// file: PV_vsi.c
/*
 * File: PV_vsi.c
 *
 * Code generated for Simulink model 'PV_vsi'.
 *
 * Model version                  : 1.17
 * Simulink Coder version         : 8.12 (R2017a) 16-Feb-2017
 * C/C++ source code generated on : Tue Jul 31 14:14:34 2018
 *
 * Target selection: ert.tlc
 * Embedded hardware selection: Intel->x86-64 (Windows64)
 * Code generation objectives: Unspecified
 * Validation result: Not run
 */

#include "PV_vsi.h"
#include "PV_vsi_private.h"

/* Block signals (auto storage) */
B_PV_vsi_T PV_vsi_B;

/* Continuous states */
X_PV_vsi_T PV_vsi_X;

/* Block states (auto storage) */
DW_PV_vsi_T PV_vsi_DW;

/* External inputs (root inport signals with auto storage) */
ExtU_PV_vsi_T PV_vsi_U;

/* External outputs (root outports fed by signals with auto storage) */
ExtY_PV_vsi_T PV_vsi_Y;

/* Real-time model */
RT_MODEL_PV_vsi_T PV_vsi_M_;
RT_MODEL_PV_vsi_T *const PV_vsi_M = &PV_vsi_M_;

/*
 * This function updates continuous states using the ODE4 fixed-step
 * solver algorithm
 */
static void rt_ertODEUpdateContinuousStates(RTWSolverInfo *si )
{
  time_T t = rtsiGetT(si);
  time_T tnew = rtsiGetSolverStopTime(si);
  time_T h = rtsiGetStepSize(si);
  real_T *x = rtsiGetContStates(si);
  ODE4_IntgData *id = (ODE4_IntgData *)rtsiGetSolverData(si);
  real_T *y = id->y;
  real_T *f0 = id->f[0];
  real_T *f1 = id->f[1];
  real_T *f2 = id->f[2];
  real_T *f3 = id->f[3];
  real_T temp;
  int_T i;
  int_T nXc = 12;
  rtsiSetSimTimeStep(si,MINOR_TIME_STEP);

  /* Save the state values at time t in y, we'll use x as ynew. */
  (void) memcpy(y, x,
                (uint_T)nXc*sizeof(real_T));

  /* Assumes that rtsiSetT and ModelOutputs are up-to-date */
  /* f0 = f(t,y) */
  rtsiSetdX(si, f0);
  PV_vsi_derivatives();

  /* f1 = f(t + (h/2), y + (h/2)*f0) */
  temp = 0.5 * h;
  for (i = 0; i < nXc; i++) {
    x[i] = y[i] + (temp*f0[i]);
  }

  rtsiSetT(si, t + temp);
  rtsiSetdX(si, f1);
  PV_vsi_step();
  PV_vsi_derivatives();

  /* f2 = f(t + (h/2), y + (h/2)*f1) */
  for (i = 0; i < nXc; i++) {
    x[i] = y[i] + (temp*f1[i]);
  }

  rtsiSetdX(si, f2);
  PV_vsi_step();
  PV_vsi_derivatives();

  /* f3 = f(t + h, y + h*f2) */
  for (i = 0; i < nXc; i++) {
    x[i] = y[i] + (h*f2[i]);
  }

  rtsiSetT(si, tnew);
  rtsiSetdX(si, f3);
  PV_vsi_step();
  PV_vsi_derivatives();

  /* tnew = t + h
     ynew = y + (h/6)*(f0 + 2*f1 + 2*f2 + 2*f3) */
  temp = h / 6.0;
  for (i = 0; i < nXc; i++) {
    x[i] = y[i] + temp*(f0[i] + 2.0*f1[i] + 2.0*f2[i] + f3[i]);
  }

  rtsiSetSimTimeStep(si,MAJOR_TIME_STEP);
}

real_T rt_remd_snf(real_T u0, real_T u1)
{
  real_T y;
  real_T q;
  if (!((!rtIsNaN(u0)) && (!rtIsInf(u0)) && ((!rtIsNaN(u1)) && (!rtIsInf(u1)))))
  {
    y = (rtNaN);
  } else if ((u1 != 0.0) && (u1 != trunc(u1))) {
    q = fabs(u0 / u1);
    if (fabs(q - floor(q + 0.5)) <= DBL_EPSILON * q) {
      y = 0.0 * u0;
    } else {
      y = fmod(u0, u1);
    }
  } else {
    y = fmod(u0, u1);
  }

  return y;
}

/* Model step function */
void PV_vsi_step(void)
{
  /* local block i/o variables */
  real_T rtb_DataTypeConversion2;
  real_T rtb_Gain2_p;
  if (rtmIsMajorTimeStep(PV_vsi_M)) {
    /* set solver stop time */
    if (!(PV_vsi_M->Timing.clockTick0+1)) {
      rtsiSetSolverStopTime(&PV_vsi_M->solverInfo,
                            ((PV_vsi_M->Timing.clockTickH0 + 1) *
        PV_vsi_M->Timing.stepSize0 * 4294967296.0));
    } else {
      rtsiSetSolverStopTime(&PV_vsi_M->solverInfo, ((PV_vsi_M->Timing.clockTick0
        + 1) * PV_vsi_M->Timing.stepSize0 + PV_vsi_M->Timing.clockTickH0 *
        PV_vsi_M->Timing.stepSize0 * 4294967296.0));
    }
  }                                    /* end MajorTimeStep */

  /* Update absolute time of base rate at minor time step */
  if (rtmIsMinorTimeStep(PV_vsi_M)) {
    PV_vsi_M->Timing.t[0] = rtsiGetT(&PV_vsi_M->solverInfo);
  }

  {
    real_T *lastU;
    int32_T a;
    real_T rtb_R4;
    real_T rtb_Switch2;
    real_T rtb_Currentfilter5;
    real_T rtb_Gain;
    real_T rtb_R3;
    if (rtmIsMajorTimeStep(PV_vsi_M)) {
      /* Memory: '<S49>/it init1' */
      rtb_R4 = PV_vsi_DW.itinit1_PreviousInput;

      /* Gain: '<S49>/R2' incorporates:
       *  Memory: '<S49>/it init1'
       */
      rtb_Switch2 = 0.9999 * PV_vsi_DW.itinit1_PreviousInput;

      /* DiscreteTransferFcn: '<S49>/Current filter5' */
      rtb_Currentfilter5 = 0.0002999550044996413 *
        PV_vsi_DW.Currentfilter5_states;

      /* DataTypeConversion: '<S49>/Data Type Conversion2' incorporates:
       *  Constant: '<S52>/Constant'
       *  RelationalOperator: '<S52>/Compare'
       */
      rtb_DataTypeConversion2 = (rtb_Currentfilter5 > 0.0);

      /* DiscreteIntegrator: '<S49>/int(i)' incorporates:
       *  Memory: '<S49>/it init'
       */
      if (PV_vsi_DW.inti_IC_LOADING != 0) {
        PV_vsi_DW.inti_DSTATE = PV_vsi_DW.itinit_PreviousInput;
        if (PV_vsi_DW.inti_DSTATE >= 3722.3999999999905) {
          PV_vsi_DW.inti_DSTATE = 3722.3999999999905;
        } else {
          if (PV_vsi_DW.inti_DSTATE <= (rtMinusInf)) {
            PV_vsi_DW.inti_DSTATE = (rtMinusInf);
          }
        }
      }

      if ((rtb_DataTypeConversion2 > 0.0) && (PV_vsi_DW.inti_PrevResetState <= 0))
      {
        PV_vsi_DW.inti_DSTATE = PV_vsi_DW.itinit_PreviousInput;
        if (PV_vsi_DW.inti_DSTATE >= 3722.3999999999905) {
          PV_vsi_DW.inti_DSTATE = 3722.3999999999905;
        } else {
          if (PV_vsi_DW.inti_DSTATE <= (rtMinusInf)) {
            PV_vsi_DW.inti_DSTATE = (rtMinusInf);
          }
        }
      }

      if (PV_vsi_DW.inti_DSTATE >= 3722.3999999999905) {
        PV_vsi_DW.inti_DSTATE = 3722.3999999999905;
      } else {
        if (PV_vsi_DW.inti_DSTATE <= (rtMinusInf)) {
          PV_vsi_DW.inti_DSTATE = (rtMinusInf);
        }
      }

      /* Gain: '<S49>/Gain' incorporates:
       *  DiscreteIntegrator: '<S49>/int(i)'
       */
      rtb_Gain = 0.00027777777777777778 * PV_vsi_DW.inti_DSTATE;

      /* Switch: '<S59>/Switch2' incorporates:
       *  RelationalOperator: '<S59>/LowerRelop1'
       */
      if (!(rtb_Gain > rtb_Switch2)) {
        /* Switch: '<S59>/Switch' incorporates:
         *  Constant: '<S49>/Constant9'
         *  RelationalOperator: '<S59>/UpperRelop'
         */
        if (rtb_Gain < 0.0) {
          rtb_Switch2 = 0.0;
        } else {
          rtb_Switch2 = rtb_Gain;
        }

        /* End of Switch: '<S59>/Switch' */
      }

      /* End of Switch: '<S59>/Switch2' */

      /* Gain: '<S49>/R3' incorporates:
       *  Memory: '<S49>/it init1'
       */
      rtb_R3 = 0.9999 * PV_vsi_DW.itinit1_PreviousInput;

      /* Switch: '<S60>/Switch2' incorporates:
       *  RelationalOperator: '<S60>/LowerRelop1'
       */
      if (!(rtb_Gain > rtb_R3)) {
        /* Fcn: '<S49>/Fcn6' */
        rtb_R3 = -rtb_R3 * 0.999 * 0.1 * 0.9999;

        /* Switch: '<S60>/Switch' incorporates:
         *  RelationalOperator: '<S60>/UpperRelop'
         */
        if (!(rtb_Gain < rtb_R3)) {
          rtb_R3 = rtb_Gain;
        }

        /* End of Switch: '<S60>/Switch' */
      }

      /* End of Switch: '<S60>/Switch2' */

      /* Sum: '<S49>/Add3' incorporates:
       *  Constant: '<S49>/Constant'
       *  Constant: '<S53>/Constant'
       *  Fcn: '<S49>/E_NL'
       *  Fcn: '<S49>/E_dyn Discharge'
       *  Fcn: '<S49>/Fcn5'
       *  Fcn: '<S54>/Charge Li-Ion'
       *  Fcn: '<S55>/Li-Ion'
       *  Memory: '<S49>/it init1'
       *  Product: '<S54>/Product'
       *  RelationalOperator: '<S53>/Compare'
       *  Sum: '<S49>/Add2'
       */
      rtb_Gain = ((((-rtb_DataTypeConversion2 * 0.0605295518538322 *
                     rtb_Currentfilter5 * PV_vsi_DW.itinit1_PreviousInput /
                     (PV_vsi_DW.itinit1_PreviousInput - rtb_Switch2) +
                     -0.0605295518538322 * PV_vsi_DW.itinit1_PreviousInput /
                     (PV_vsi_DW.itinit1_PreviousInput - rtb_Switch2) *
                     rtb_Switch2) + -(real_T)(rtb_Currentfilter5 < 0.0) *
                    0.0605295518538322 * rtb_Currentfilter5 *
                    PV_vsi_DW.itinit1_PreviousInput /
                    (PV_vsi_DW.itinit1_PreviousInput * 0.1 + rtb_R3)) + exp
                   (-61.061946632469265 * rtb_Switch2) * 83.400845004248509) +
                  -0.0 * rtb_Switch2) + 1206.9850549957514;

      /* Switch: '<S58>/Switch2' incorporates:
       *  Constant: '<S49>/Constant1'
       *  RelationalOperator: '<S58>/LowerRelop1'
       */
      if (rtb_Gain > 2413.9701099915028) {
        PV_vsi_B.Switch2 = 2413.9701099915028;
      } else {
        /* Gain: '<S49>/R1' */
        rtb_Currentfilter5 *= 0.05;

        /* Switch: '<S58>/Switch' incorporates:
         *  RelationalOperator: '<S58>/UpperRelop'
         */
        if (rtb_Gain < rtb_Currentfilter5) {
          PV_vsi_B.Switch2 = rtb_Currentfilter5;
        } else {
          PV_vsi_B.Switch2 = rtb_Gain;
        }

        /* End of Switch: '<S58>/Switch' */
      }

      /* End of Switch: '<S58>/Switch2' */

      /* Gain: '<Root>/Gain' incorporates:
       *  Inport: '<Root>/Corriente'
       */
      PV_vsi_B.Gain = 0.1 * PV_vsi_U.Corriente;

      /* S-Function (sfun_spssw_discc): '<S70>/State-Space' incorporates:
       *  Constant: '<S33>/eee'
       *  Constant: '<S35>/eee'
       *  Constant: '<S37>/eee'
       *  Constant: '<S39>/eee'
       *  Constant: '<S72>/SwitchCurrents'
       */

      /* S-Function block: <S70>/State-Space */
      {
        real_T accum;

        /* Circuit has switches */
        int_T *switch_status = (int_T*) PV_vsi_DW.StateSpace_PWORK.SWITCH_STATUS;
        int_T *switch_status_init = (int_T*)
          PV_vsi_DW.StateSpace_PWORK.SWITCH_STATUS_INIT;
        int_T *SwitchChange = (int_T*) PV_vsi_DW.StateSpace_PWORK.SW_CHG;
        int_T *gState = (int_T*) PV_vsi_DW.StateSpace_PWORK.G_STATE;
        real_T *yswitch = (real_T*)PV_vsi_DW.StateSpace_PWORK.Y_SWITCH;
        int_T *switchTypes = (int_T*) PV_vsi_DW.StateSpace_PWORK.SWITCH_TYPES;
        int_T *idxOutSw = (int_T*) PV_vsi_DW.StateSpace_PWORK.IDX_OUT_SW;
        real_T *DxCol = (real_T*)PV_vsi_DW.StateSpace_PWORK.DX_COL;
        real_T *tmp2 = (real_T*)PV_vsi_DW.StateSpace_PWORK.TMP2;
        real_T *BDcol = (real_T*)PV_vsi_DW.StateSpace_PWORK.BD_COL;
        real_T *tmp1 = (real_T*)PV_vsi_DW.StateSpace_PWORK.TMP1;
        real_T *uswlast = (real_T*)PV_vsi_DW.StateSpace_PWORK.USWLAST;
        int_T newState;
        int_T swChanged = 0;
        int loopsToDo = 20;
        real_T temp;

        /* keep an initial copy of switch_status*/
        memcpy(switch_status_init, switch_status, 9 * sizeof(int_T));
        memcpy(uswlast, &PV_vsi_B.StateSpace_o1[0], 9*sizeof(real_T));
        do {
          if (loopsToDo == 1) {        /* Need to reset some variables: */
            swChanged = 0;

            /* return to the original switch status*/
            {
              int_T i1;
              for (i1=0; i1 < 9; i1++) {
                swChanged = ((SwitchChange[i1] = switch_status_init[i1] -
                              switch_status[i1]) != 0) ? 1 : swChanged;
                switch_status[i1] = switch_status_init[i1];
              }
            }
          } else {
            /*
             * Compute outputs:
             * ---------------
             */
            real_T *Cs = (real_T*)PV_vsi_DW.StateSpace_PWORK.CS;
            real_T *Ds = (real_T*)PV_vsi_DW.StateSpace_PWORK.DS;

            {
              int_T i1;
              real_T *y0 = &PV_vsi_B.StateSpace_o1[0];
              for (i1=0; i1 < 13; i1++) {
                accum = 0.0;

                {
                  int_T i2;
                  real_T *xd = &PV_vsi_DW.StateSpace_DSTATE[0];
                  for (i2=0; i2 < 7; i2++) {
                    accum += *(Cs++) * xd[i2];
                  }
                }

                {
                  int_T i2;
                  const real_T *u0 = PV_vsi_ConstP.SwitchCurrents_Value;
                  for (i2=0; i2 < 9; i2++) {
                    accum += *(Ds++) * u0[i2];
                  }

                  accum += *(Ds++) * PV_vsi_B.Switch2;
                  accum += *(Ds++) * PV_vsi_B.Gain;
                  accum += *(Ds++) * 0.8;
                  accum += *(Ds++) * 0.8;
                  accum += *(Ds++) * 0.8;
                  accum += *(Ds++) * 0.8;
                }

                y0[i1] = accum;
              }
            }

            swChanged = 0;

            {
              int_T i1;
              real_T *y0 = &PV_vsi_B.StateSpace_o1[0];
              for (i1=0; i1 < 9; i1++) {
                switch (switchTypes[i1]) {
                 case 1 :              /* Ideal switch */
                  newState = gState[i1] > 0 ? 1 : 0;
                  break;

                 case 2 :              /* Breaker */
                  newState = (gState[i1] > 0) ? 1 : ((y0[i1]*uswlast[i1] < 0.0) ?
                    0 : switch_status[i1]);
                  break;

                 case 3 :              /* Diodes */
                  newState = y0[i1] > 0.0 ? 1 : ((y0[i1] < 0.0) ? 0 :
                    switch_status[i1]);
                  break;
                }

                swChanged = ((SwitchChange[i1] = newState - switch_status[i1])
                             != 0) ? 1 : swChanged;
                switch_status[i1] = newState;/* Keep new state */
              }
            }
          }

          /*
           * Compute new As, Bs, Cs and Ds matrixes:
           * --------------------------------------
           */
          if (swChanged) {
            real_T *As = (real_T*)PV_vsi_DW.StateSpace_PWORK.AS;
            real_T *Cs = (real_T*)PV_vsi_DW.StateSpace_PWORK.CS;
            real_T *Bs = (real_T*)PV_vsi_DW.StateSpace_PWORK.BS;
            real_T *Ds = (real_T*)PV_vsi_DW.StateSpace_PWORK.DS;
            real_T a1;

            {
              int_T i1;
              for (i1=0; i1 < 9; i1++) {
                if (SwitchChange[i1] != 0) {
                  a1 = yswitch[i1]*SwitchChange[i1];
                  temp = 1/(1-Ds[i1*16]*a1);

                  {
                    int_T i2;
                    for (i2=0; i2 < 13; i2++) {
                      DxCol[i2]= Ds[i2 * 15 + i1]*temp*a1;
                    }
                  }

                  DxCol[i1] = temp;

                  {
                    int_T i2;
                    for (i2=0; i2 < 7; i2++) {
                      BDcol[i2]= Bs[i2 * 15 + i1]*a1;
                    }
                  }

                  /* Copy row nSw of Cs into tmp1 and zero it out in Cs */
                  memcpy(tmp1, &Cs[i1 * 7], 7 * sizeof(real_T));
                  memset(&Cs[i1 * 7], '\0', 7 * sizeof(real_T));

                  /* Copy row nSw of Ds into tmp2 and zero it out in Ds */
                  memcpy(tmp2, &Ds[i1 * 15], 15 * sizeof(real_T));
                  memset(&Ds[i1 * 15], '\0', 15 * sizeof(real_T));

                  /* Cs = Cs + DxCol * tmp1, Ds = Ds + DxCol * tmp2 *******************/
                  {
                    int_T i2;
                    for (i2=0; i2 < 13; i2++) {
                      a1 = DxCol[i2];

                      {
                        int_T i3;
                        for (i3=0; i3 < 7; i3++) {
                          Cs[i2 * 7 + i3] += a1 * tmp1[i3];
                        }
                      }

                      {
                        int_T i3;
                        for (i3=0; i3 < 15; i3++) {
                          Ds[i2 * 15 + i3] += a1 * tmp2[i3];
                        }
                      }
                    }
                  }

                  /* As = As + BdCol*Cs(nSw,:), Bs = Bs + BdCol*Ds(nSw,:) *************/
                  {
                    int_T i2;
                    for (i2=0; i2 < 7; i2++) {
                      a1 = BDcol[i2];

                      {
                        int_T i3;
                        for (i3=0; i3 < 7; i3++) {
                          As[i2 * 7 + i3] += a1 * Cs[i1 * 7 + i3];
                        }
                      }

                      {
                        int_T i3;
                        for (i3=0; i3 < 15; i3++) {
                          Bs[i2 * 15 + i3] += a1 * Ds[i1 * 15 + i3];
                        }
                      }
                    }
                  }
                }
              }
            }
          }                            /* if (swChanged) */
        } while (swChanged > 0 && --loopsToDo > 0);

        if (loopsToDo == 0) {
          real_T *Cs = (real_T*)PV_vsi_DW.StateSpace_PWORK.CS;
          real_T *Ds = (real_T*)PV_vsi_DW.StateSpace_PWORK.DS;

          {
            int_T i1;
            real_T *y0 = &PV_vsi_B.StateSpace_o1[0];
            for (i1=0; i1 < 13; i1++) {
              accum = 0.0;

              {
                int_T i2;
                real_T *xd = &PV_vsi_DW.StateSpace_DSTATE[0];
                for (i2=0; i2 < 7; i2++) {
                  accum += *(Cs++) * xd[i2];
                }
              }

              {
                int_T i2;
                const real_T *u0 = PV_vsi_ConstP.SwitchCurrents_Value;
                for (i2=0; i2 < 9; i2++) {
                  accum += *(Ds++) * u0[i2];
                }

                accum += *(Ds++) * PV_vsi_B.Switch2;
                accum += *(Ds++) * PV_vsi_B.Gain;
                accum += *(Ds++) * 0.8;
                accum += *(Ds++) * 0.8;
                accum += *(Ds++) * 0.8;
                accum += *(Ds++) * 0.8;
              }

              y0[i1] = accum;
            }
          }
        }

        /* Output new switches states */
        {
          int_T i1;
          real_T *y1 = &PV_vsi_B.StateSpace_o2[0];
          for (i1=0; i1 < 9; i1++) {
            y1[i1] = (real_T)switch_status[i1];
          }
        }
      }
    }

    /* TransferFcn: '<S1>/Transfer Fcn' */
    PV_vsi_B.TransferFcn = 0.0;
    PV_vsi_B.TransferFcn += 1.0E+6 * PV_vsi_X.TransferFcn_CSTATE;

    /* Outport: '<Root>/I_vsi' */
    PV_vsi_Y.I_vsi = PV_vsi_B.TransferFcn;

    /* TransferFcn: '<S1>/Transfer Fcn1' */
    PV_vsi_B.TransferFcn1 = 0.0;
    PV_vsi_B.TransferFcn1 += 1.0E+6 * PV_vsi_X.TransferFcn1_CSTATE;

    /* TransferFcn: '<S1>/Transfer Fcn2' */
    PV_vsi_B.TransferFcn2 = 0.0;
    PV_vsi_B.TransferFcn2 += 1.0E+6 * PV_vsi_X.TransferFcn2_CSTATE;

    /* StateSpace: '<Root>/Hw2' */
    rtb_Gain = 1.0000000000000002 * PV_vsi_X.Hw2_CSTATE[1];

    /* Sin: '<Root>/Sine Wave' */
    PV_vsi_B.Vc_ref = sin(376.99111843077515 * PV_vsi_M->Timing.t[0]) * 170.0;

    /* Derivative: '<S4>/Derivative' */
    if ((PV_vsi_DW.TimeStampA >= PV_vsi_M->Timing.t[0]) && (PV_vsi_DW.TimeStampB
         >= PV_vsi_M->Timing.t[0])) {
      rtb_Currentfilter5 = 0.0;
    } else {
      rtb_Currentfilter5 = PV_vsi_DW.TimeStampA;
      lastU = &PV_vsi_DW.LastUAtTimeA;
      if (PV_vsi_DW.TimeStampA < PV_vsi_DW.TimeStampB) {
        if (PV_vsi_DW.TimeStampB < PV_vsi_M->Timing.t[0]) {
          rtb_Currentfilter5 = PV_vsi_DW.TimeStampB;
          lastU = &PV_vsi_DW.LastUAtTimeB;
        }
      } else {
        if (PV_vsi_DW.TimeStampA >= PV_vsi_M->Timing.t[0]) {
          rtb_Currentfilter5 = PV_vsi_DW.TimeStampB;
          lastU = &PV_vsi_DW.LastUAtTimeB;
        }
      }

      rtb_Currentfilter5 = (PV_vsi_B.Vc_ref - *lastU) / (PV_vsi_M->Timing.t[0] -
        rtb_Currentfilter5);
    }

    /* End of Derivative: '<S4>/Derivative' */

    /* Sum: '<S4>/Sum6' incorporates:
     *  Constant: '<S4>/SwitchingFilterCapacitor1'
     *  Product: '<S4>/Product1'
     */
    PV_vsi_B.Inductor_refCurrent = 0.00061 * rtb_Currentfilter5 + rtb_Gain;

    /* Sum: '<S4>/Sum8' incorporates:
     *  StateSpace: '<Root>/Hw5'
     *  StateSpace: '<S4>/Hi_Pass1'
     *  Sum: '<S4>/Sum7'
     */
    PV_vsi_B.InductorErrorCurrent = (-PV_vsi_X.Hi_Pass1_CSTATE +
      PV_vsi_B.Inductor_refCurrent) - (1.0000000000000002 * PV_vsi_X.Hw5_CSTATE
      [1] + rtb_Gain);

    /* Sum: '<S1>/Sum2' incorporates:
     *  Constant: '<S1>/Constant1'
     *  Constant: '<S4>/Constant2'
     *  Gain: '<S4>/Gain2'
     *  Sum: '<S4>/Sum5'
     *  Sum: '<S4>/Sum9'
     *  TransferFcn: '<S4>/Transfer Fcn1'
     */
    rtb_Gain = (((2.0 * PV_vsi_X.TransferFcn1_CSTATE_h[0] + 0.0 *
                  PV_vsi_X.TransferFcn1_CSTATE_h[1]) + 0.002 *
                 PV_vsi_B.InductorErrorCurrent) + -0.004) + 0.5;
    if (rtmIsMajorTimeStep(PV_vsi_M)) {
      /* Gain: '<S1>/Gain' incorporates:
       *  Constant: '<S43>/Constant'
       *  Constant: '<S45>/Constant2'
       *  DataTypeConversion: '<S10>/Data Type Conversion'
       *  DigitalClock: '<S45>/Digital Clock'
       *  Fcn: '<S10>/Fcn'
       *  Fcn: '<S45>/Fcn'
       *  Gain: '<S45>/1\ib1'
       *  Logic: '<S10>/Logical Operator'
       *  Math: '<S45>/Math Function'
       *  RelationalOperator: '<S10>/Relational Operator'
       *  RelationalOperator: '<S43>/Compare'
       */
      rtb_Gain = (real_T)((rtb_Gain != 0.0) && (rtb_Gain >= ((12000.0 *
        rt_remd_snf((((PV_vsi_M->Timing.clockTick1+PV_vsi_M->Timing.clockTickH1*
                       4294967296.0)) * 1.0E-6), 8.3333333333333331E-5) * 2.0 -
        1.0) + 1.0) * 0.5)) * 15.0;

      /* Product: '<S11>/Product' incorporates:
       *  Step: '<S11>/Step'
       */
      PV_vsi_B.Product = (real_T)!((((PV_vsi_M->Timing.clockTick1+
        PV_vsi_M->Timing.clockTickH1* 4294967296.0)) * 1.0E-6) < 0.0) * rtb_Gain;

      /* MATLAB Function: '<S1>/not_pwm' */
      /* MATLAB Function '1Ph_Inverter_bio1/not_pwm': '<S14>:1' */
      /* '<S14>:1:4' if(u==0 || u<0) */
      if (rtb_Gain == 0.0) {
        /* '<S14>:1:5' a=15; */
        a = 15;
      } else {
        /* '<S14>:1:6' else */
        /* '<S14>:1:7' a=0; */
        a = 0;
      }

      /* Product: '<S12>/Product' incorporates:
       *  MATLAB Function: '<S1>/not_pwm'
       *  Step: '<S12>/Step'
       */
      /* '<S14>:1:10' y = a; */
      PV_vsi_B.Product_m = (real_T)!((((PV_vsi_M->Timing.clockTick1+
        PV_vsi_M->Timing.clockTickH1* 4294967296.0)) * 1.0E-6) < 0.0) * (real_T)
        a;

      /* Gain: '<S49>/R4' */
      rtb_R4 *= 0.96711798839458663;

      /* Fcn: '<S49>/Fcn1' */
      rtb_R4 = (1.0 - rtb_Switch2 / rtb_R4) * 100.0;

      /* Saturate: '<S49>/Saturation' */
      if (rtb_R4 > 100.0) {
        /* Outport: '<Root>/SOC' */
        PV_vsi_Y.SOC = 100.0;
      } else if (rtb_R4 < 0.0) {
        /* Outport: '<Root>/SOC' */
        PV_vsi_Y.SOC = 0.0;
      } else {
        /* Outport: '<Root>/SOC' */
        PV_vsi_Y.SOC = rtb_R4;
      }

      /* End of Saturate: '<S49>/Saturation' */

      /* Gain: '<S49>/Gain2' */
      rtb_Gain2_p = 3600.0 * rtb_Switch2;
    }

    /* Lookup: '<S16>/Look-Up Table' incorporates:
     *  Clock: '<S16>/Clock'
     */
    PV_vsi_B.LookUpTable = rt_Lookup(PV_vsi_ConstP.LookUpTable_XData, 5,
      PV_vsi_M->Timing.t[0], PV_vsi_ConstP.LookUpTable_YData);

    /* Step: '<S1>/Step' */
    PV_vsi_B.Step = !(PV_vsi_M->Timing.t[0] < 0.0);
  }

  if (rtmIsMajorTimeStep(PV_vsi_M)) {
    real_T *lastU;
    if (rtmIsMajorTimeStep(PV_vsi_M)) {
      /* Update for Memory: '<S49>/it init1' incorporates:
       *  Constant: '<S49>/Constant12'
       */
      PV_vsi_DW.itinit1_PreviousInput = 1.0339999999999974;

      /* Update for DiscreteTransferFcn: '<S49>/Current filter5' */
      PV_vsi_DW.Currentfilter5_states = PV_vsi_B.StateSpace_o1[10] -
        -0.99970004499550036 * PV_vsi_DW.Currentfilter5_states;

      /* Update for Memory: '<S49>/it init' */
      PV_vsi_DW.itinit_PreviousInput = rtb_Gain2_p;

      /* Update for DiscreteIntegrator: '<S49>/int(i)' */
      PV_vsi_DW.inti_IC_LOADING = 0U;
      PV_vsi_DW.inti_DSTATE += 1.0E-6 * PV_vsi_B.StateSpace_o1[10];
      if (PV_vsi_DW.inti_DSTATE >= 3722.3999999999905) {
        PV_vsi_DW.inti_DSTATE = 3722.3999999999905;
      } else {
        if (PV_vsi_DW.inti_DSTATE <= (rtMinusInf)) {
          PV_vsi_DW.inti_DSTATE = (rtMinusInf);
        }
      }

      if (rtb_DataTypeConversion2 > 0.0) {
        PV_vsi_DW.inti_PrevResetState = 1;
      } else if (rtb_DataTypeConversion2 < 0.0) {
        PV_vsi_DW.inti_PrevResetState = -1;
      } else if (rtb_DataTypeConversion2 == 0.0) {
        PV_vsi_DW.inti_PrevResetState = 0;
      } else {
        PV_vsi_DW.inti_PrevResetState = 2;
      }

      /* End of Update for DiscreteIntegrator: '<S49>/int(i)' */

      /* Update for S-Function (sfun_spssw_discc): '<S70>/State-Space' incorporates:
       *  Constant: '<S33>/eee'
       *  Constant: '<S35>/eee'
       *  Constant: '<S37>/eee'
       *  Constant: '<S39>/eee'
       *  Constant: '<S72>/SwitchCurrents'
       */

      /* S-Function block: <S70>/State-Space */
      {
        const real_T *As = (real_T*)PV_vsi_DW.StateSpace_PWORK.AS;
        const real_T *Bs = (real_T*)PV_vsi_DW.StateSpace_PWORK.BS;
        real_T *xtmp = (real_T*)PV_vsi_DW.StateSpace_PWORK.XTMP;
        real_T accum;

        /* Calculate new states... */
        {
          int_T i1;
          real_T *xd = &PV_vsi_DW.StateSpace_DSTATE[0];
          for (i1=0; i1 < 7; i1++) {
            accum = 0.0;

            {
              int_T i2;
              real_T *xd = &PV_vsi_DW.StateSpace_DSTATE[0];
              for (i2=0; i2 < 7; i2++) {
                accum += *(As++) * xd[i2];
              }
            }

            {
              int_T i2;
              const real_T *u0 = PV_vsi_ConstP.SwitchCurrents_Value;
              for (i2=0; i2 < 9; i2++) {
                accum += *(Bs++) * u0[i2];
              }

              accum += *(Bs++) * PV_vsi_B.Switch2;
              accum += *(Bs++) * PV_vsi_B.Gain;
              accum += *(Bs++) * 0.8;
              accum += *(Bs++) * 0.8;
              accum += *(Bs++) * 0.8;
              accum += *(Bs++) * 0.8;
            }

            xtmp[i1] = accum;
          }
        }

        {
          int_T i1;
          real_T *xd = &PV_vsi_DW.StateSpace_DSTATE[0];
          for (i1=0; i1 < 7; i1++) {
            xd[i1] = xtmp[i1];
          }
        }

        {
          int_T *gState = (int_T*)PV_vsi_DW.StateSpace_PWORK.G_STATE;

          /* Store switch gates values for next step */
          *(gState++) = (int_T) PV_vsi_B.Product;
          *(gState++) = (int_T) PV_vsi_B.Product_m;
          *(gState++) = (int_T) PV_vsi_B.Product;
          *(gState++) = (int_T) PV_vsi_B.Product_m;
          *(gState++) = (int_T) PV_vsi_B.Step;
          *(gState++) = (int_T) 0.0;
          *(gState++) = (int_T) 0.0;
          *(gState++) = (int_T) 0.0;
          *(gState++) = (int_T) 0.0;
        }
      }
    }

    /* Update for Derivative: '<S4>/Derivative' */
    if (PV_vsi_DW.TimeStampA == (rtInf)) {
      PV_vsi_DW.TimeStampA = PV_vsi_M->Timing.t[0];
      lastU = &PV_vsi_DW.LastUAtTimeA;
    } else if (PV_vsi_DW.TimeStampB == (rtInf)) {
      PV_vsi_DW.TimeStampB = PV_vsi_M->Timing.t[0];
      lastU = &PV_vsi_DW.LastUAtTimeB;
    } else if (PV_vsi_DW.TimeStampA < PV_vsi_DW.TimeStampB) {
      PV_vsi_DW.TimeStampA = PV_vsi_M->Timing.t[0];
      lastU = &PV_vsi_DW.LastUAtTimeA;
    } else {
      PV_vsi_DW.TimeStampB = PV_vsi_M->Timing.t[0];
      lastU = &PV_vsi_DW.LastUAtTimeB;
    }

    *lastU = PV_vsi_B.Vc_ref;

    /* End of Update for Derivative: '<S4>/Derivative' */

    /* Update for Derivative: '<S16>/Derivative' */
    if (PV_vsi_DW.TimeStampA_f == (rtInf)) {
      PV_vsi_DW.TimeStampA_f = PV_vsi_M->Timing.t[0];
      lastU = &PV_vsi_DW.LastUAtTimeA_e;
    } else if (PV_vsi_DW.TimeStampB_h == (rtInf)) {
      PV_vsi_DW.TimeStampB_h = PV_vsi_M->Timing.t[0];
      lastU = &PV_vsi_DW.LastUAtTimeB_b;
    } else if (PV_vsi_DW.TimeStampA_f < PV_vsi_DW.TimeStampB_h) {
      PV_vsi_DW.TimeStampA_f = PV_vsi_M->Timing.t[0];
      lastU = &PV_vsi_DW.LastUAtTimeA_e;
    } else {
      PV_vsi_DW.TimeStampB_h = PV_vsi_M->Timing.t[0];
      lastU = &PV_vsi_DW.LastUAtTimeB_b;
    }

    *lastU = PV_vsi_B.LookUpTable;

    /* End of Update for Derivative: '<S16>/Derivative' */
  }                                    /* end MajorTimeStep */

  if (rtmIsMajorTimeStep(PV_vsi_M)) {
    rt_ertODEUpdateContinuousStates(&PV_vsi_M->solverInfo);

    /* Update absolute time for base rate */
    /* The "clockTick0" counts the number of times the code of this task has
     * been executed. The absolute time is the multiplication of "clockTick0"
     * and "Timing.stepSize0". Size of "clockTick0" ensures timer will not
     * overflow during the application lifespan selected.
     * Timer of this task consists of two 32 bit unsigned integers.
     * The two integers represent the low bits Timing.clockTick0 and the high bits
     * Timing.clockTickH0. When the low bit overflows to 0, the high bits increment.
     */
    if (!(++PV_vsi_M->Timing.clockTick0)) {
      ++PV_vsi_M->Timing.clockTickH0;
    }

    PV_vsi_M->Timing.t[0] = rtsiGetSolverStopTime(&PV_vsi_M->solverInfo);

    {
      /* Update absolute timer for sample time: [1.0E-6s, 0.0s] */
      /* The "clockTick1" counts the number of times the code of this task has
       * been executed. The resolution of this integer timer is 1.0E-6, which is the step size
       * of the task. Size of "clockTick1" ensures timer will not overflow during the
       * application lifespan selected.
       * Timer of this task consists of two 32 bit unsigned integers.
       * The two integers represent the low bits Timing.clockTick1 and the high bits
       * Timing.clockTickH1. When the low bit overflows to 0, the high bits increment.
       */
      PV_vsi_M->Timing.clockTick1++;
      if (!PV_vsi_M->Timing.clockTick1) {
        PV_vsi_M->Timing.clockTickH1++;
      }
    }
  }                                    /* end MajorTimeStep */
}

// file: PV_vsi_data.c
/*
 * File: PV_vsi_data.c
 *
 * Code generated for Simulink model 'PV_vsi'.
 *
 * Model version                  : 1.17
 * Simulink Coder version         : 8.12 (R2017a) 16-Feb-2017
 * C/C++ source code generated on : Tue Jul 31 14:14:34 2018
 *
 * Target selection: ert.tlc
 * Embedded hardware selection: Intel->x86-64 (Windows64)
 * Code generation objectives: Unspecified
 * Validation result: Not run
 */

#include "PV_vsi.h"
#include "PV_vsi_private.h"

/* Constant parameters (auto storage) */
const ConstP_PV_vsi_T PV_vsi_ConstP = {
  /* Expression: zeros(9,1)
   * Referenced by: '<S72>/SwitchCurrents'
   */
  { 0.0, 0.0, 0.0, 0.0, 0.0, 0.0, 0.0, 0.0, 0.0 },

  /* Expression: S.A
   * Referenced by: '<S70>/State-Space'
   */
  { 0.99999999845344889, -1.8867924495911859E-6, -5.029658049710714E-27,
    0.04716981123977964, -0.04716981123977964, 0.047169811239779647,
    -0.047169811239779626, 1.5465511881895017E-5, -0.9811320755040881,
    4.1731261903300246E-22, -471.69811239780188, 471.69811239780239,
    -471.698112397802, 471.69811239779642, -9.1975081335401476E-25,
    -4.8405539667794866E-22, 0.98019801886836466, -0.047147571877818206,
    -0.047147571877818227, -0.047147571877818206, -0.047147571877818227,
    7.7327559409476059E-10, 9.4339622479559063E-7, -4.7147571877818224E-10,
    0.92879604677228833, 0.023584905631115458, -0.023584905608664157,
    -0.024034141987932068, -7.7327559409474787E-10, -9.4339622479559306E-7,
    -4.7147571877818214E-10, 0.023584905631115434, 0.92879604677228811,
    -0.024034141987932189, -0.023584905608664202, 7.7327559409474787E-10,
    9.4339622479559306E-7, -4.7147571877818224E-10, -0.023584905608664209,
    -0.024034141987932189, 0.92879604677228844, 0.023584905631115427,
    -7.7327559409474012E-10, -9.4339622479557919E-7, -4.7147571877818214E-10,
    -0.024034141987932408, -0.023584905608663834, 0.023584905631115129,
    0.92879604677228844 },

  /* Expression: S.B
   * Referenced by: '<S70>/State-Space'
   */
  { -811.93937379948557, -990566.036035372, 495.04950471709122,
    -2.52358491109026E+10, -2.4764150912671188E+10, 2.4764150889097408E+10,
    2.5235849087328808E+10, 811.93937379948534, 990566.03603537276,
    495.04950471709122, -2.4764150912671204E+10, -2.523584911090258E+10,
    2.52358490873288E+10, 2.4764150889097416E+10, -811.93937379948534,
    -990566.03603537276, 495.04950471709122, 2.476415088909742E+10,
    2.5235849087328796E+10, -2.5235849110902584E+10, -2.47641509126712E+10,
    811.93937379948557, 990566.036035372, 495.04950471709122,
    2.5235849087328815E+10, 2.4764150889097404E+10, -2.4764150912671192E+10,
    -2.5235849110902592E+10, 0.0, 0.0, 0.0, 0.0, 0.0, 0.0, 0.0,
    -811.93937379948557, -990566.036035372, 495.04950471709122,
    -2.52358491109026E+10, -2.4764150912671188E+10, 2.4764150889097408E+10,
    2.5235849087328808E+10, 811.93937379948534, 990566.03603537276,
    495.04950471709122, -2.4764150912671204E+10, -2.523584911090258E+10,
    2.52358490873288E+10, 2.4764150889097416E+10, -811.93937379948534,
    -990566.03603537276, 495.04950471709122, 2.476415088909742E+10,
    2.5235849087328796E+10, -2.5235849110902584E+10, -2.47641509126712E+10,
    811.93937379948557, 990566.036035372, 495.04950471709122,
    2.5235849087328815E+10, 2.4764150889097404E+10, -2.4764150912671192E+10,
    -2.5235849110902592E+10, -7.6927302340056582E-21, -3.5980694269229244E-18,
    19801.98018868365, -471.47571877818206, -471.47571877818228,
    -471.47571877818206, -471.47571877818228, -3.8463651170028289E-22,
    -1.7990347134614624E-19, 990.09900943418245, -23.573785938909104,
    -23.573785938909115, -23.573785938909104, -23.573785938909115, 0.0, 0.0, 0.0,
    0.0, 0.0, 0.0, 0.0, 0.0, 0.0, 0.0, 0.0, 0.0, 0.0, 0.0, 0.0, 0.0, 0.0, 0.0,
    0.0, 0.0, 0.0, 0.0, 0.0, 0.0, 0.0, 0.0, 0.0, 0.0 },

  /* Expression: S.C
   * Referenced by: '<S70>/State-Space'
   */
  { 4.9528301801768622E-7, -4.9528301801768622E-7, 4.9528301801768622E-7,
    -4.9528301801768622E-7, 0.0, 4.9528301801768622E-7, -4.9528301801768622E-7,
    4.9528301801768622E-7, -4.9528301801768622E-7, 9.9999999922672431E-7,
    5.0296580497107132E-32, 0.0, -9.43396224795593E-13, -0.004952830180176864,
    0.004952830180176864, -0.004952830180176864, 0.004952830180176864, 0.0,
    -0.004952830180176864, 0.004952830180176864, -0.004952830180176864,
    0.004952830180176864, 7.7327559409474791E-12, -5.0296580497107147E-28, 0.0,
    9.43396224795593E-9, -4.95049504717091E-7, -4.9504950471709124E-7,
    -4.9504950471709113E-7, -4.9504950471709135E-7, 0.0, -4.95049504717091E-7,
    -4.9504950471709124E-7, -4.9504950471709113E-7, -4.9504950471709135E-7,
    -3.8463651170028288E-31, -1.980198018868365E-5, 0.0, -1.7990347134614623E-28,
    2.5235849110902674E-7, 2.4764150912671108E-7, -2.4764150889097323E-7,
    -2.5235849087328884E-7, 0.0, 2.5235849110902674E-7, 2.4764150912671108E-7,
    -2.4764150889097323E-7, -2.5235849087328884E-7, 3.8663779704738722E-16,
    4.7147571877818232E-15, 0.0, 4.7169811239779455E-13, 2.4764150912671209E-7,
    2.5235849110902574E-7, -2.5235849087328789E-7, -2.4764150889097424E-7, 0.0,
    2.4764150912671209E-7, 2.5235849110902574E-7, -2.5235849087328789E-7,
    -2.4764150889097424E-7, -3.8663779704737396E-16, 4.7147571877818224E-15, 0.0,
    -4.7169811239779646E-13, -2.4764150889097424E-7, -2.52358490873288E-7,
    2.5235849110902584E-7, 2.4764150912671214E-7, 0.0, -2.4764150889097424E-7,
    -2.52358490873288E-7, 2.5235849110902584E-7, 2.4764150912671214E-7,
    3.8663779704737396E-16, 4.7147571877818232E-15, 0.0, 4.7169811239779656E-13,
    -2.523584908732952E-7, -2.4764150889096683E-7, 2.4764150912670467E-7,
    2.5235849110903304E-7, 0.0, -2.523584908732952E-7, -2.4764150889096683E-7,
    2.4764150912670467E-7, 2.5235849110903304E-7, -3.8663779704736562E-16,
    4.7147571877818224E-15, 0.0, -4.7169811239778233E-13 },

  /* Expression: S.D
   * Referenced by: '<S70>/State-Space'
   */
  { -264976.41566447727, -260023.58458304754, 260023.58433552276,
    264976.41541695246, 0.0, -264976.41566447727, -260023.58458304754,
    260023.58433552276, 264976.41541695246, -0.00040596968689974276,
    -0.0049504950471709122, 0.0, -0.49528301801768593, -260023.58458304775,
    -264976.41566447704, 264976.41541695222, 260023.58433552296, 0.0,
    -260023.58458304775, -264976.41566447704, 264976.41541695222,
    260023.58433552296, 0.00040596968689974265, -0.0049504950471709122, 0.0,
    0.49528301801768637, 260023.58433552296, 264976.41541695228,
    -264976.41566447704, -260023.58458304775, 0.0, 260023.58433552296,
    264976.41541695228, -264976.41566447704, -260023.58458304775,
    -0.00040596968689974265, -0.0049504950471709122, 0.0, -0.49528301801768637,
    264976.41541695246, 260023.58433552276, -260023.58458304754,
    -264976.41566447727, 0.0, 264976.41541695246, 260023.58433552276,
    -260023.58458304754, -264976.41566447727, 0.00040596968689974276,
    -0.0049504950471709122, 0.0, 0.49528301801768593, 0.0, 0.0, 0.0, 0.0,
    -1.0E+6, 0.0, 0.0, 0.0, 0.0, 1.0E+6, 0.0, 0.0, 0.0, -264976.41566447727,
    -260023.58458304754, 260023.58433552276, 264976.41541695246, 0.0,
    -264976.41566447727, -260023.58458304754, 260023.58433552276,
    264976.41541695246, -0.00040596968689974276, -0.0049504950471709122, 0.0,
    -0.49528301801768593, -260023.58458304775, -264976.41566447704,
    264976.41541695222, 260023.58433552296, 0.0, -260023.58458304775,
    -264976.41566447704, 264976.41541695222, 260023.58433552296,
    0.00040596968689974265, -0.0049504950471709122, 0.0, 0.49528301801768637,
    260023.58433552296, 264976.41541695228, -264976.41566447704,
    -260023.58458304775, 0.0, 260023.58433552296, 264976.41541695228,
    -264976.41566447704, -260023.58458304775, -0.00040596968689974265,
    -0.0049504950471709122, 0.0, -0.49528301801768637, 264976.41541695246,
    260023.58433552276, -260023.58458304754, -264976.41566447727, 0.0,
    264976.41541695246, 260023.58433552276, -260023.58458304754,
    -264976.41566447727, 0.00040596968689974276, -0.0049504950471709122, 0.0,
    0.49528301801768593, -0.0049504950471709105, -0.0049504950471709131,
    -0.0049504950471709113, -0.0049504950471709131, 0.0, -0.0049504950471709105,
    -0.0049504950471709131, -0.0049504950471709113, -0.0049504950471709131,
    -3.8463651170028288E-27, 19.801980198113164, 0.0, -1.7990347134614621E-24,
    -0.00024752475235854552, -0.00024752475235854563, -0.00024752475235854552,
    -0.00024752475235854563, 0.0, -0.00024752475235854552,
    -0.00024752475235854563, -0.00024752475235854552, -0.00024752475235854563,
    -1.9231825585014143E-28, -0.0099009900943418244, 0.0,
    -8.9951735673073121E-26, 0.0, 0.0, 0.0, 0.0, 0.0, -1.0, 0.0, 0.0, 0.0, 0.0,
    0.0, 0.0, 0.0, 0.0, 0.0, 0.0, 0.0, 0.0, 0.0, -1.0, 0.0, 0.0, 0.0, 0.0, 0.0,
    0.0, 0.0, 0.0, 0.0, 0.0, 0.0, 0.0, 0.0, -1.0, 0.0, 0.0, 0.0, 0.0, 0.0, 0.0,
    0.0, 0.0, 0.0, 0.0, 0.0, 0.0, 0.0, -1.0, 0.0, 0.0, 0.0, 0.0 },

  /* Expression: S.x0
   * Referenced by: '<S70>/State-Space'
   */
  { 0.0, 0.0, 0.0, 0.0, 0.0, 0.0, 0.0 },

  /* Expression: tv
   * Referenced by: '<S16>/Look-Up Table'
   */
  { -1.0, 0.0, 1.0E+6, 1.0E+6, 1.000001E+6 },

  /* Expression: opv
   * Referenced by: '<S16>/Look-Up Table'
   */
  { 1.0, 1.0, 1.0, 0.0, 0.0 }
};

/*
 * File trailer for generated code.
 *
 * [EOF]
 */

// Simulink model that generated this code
simulink model "PV_vsi"  (R2017a)
settings: Solver=ode4  StartTime=0.0  StopTime=10.0  FixedStep=1e-6  MaxStep=1e-4  RelTol=1e-3
InitFcn:
  | SimulinkInit
undefined symbols (not defined in the file or in its folder): Ion, Lithium
libraries: powerlib x17, dsparch4 x4, powerlib_meascontrol x1, electricdrivelib x1

== system PV_vsi ==
  note: Renewable Source as VSI converter
  Corriente : Inport
  1Ph_Inverter_bio1 : Subsystem  mask{st_time=0, f_sw=12000, samp_f=1e-6}
      mask prompts: st_time "Tiempo muerto (Start)"; f_sw "Switching frequency"; samp_f "samplig"
  Battery : electricdrivelib/Extra Sources/Battery  BatType=Lithium-Ion  ShowTempParam=off  ThermalPreset=no  ShowAgeParam=off  NomV=1100  NomQ=.5  SOC=100  Batt_Tr=10e-3  PresetModel=off  MaxQ=1  MinV=825  FullV=1280.3859  Dis_rate=200  R=50e-3  Normal_OP=0.90435  expZone="[1188.4244    0.049130435]"  current=[6.5 13 32.5 50]  Units=Time  Tci=20  NomT=20  T2=-30  MaxQ2=4.8  FullV2=7.1  Normal_OP2=5.655  expZone2="[6.58           1]"  Rca=0.6  ti=2000  Dp=0  Neq0=0  Tsim=1e6  Ta1=25  Qeol=5.4*0.9  Reol=0.013333*1.2  Char_age=[2.3478, 3]  Dis_age=[2.3478, 10]  N1=1500  N2=10500  N3=1000  N4=1400  Ta2=45  N5=950
  Bus Selector : BusSelector  OutputSignals=SOC (%),Current (A),Voltage (V)
  Controlled Current Source : powerlib/Electrical Sources/Controlled Current Source  Initialize=on  Source_Type=AC  Amplitude=0  Phase=0  Frequency=0  Measurements=None
  Gain : Gain  Gain=1/10
  Hw2 : dsparch4/Analog Filter Design  method=Bessel  filttype=Lowpass  N=2  Wlo=7000*2*pi  Whi=80  Rp=2  Rs=80
  Hw5 : dsparch4/Analog Filter Design  method=Bessel  filttype=Lowpass  N=2  Wlo=7000*2*pi  Whi=80  Rp=2  Rs=80
  Hw6 : dsparch4/Analog Filter Design  method=Bessel  filttype=Lowpass  N=2  Wlo=7000*2*pi  Whi=80  Rp=2  Rs=80
  Rin2 : powerlib/Elements/Series RLC Branch  LConnTagsString=__new0  RConnTagsString=__new0  BranchType=C  Resistance=.001  Inductance=0  SetiL0=off  InitialCurrent=0  Capacitance=1000e-6  Setx0=off  InitialVoltage=0  Measurements=None
  Sine Wave : Sin  Amplitude=170  Frequency=2*pi*60  SampleTime=0
  VSI_Controller : Subsystem
  powergui : powerlib/powergui  Priority=1  SimulationMode=Discrete  SampleTime=1e-6  frequency=60  Iterations=50  frequencyindice=0  Pbase=100e6  ErrMax=1e-4  UnitsV=kV  UnitsW=MW  buscounter=0  FunctionMessages=off  echomessages=off  EnableUseOfTLC=off  CurrentSourceSwitches=off  DisableSnubberDevices=off  DisableRonSwitches=off  DisableVfSwitches=off  DisplayEquations=off  SolverType=Tustin/Backward Euler (TBE)  Interpol=off  ExternalGateDelay=off  methode=off  Ts=100  x0status=blocks  SPID=on  SwTol=0  HookPort=off  RestoreLinks=warning  ResistiveCurrentMeasurement=off  Frange=[0:2:500]  Ylog=off  Xlog=on  ShowGrid=off  save=off  variable=ZData  structure=0  ZoomFFT=off  StartTime=0.0  cycles=1  DisplayStyle=1  fundamental=60  FreqAxis=off  MaxFrequency=1000  frequencyindicesteady=1  RmsSteady=1  display=off
  I_vsi : Outport
  SOC : Outport  Port=2
  wires:
  Hw6/1 -> [V_vsi]
  [D_vsi] -> 1Ph_Inverter_bio1/1(A_in)
  1Ph_Inverter_bio1/2(Vout) -> Hw6/1
  Sine Wave/1 -> VSI_Controller/2(Ref Voltage)  "Vc_ref"
  Hw5/1 -> [I_cap_vsi]
  1Ph_Inverter_bio1/3(I cap) -> Hw5/1
  VSI_Controller/1(d) -> [D_vsi]
  Gain/1 -> Controlled Current Source/1
  Battery/1 -> Bus Selector/1
  1Ph_Inverter_bio1/1(Iout) -> I_vsi/1, Hw2/1
  Hw2/1 -> [I_vsi]
  [I_cap_vsi] -> VSI_Controller/3(Capacitor Current)
  Bus Selector/1 -> SOC/1  "<SOC (%)>"
  [I_vsi] -> VSI_Controller/1(Output Current)  "OutputCurrent"
  Corriente/1 -> Gain/1
  connections:
  1Ph_Inverter_bio1/LConn2 -- Battery/LConn2 -- Controlled Current Source/LConn1 -- Rin2/RConn1
  Battery/LConn1 -- Controlled Current Source/RConn1 -- 1Ph_Inverter_bio1/LConn1 -- Rin2/LConn1

== system PV_vsi/1Ph_Inverter_bio1 ==
  note: Gate Drivers: Generan las señales cuadradas para
      | la conmutacion del convertidor de 3 brazos e implementan el
      | tiempo muerto para mejorar la calidad de la simulacion
  A_in : Inport
  Breaker : powerlib/Elements/Breaker  InitialState=0  SwitchingTimes="[1/60  5/60]"  External=on  BreakerResistance=0.01  SnubberResistance=1e6  SnubberCapacitance=inf  Measurements=None  MoreParameters=on  NoBreakLoop=off
  Cf : powerlib/Elements/Series RLC Branch  LConnTagsString=__new0  RConnTagsString=__new0  BranchType=C  Resistance=1  Inductance=1e-3  SetiL0=off  InitialCurrent=0  Capacitance=610e-6  Setx0=off  InitialVoltage=0  Measurements=None
  Constant1 : Constant  Value=0.5
  Gain : Gain  Gain=15
  H bridge : Subsystem
  I sens A : powerlib/Measurements/Current Measurement  PhasorSimulation=off  OutputType=Complex  PSBequivalent=0
  I sens A1 : powerlib/Measurements/Current Measurement  PhasorSimulation=off  OutputType=Complex  PSBequivalent=0
  Lf : powerlib/Elements/Series RLC Branch  LConnTagsString=__new0  RConnTagsString=__new0  BranchType=RL  Resistance=1e-3  Inductance=5e-3  SetiL0=off  InitialCurrent=0  Capacitance=1e-6  Setx0=off  InitialVoltage=0  Measurements=None
  PWM Generator (DC-DC) : powerlib_meascontrol/Pulse & Signal Generators/PWM Generator (DC-DC)  Fsw=f_sw  Ts=samp_f
  Step : Step  Time=st_time  SampleTime=0
  Steper1 : Subsystem
  Steper3 : Subsystem
  Sum2 : Sum
  Transfer Fcn : TransferFcn  Denominator=[1e-6 1]
  Transfer Fcn1 : TransferFcn  Denominator=[1e-6 1]
  Transfer Fcn2 : TransferFcn  Denominator=[1e-6 1]
  Vsensa1 : powerlib/Measurements/Voltage Measurement  PhasorSimulation=off  OutputType=Complex  PSBequivalent=0
  not_pwm : MATLAB Function  TreatAsAtomicUnit=on
  Collector : PMIOPort  Port=1  Side=Left
  Emitter : PMIOPort  Port=2  Side=Left
  Iout : Outport
  Vout : Outport  Port=2
  I cap : Outport  Port=3
  wires:
  not_pwm/1(y) -> Steper3/1(In1)
  Sum2/1 -> PWM Generator (DC-DC)/1
  PWM Generator (DC-DC)/1 -> Gain/1
  Constant1/1 -> Sum2/2
  A_in/1 -> Sum2/1
  Steper1/1(Out1) -> [pwma]
  Steper3/1(Out1) -> [Npwma]
  Gain/1 -> Steper1/1(In1), not_pwm/1(u)
  [pwma] -> H bridge/1(Ahi)
  [Npwma] -> H bridge/2(Bhi), H bridge/3(Alo)
  [pwma] -> H bridge/4(Blo)
  I sens A/1 -> Transfer Fcn/1  "A_current"
  Vsensa1/1 -> Transfer Fcn1/1  "A_volts"
  Transfer Fcn/1 -> Iout/1
  Transfer Fcn1/1 -> Vout/1
  Step/1 -> Breaker/1
  Transfer Fcn2/1 -> I cap/1
  I sens A1/1 -> Transfer Fcn2/1  "Ic"
  connections:
  H bridge/RConn3 -- Collector/RConn1
  H bridge/RConn4 -- Emitter/RConn1
  Lf/LConn1 -- H bridge/RConn1
  H bridge/RConn2 -- Vsensa1/LConn2 -- Cf/RConn1
  Breaker/LConn1 -- I sens A/RConn1
  Vsensa1/LConn1 -- Breaker/RConn1
  I sens A/LConn1 -- Lf/RConn1 -- I sens A1/LConn1
  I sens A1/RConn1 -- Cf/LConn1

== system PV_vsi/VSI_Controller ==
  Output Current : Inport
  Ref Voltage : Inport  Port=2
  Capacitor Current : Inport  Port=3
  Constant2 : Constant  Value=-4e-3
  Derivative : Derivative  CoefficientInTFapproximation=1e-3
  Gain2 : Gain  Gain=.002
  Hi_Pass1 : dsparch4/Analog Filter Design  method=Bessel  filttype=Highpass  N=1  Wlo=1*2*pi  Whi=80  Rp=2  Rs=40
  Product1 : Product
  Scope7 : Scope  NumInputPorts=2
  Scope8 : Scope  NumInputPorts=2
  Sum5 : Sum  Inputs=+|+
  Sum6 : Sum  Inputs=+|+
  Sum7 : Sum  Inputs=+|+
  Sum8 : Sum  Inputs=|+-
  Sum9 : Sum  Inputs=|++
  SwitchingFilterCapacitor1 : Constant  Value=610e-6
  Transfer Fcn1 : TransferFcn  Numerator=[2 0]  Denominator=[1 2 (2*pi*60)^2]
  d : Outport
  wires:
  Derivative/1 -> Product1/2
  Sum6/1 -> Hi_Pass1/1, Scope8/1  "Inductor_refCurrent"
  Sum8/1 -> Transfer Fcn1/1, Gain2/1  "InductorErrorCurrent"
  Ref Voltage/1 -> Derivative/1
  Constant2/1 -> Sum9/2
  Capacitor Current/1 -> Sum7/1
  Transfer Fcn1/1 -> Sum5/2
  Output Current/1 -> Sum6/1, [I_out]
  [I_out] -> Sum7/2
  Gain2/1 -> Sum5/1
  SwitchingFilterCapacitor1/1 -> Product1/1
  Hi_Pass1/1 -> Scope8/2, Sum8/1, Scope7/1
  Product1/1 -> Sum6/2  "Capacitor_ref_current"
  Sum9/1 -> d/1
  Sum5/1 -> Sum9/1
  Sum7/1 -> Scope7/2, Sum8/2  "Measured_Inductor_Current"

== system PV_vsi/1Ph_Inverter_bio1/H bridge ==
  note: Convertirdor de 3 brazos:
      |
      | Implementado usando interruptores
      | ideales para agilizar la simulacion.
      | la salida E correspone a la corriente y laa
      | tension de cada componente
      | (sea interruptor o diodo) y su respectiva
      | corriente. no tienen puerto de salida ya que no
      | son relevantes para lo que se desea simular.
      |
      | si g=0 interruptor no conduce.
      | si g=1 interruptor conduce.
      |
      | conmutacion ocurre instantaneamente sin
      | retardo.
  Ahi : Inport
  Bhi : Inport  Port=2
  Alo : Inport  Port=3
  Blo : Inport  Port=4
   sw_ahi{1..2,5..6} (4 alike) : powerlib/Power Electronics/Ideal Switch  Ron=0.1  Lon=0  IC=0  Rs=1e6  Cs=10e-12  Measurements=on
  Diode{1..3,6} (4 alike) : powerlib/Power Electronics/Diode  Ron=.2  Lon=0  Vf=0.8  IC=0  UseSnubber=0  Rs=0  Cs=0  Measurements=on
  " Vout+" : PMIOPort  Tag=PMCPort  Port=1  Side=Right
  Vout- : PMIOPort  Tag=PMCPort  Port=2  Side=Right
  Collector : PMIOPort  Tag=PMCPort  Port=3  Side=Right
  Emitter : PMIOPort  Tag=PMCPort  Port=4  Side=Right
  wires:
  Alo/1 -> " sw_ahi6"/1
  Ahi/1 -> " sw_ahi1"/1
  Blo/1 -> " sw_ahi5"/1
  Bhi/1 -> " sw_ahi2"/1
  connections:
  Diode3/RConn1 -- Vout-/RConn1 -- " sw_ahi2"/LConn1 -- Diode2/LConn1 -- " sw_ahi5"/RConn1
  Diode3/LConn1 -- Emitter/RConn1 -- Diode6/LConn1 -- " sw_ahi6"/LConn1 -- " sw_ahi5"/LConn1
  Diode2/RConn1 -- Collector/RConn1 -- " sw_ahi1"/RConn1 -- Diode1/RConn1 -- " sw_ahi2"/RConn1
  " sw_ahi6"/RConn1 -- Diode6/RConn1 -- " Vout+"/RConn1 -- Diode1/LConn1 -- " sw_ahi1"/LConn1

== system PV_vsi/1Ph_Inverter_bio1/Steper1 ==
  In1 : Inport
  Product : Product
  Step : Step  Time=st_time  SampleTime=samp_f
  Out1 : Outport
  wires:
  Step/1 -> Product/2
  In1/1 -> Product/1
  Product/1 -> Out1/1

== system PV_vsi/1Ph_Inverter_bio1/Steper3 ==
  In1 : Inport
  Product : Product
  Step : Step  Time=st_time  SampleTime=samp_f
  Out1 : Outport
  wires:
  Product/1 -> Out1/1
  In1/1 -> Product/1
  Step/1 -> Product/2

== matlab function PV_vsi/1Ph_Inverter_bio1/not_pwm ==
function y = fcn(u)
%#codegen

if(u==0 || u<0)
    a=15;
else
    a=0;
end;

y = a;
